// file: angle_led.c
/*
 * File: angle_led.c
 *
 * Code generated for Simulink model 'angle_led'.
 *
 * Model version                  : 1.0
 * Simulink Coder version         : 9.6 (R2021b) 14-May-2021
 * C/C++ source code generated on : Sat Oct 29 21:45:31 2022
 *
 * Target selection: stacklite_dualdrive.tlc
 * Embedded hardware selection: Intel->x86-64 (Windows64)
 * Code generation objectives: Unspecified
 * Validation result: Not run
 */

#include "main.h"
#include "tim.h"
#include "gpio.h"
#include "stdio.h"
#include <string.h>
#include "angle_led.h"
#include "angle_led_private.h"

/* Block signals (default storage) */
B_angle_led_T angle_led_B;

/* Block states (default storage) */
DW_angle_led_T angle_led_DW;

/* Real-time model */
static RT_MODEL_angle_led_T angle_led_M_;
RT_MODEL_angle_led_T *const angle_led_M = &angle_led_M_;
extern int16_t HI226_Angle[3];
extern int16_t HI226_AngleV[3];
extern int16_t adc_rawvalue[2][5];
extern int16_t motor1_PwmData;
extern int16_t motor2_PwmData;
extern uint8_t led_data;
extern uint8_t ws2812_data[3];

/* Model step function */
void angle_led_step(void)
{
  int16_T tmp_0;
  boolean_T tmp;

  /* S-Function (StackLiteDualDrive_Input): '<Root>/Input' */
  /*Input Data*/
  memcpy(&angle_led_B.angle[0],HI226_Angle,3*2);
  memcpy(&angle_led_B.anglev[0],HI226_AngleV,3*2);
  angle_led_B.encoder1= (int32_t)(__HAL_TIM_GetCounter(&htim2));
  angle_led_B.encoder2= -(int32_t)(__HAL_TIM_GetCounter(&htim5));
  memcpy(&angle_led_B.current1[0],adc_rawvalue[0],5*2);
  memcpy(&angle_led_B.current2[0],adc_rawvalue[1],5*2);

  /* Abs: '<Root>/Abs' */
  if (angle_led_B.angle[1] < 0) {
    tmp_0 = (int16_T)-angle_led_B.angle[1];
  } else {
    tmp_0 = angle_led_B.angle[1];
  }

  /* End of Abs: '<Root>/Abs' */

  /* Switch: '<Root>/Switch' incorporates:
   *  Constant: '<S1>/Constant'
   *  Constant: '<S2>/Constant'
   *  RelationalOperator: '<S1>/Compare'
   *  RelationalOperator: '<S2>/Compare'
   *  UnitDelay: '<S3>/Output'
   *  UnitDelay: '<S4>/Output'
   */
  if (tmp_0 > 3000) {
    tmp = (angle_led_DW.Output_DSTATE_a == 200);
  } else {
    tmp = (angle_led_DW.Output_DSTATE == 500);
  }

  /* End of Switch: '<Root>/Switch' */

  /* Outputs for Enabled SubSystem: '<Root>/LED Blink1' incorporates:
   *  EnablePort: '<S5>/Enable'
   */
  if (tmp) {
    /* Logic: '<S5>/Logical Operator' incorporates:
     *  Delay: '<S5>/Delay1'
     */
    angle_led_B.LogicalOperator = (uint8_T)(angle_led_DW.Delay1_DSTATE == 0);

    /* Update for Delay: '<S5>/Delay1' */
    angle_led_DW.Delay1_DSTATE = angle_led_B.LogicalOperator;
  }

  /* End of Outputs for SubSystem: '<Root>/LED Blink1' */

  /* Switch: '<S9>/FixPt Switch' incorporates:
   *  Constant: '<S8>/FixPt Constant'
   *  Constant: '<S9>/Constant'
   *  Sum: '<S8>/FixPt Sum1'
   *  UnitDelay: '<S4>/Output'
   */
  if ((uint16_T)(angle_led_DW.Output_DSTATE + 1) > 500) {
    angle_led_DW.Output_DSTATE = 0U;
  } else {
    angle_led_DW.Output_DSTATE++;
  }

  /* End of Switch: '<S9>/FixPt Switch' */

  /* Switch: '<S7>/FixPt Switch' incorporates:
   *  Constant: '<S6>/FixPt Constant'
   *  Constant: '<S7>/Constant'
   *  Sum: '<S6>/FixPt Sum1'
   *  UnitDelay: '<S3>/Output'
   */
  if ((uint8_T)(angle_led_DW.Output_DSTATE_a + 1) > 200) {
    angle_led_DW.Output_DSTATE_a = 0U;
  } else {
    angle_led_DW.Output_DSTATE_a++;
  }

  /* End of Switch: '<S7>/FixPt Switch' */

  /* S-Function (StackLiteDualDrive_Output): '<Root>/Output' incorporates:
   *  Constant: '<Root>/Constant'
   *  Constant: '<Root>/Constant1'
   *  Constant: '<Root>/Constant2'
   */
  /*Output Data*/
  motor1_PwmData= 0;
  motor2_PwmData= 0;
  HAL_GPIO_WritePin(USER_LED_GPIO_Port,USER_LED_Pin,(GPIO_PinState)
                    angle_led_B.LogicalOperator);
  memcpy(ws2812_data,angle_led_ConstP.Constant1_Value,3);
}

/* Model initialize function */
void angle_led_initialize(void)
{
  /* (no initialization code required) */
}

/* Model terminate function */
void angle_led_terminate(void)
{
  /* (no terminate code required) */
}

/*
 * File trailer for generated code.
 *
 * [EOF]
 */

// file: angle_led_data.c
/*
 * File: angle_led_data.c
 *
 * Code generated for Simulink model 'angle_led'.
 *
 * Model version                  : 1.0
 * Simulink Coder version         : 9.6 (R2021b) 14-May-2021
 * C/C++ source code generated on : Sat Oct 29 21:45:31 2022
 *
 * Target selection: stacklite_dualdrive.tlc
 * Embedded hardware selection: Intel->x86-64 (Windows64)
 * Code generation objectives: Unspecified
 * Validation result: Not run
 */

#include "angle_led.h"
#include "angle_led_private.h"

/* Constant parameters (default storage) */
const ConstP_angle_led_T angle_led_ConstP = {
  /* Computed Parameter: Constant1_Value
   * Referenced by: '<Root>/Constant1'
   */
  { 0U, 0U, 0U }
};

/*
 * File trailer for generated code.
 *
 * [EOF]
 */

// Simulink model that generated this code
simulink model "angle_led"  (R2021b)
settings: Solver=FixedStepDiscrete  StartTime=0.0  StopTime=inf  FixedStep=0.0005  RelTol=1e-3
libraries: simulink x4

== system angle_led ==
  note: angle的单位是0.01度，
      | 即30度输出值为3000
  Abs : Abs
  Compare To Constant : simulink/Logic and Bit Operations/Compare To Constant  relop===  const=200  OutDataTypeStr=boolean
  Compare To Constant1 : simulink/Logic and Bit Operations/Compare To Constant  relop===  const=500  OutDataTypeStr=boolean
  Constant : Constant  Value=0  OutDataTypeStr=int16
  Constant1 : Constant  Value=[0 0 0]  OutDataTypeStr=uint8
  Constant2 : Constant  Value=0  OutDataTypeStr=int16
  Counter Limited : simulink/Sources/Counter Limited  uplimit=200  tsamp=-1
  Counter Limited1 : simulink/Sources/Counter Limited  uplimit=500  tsamp=-1
  Demux : Demux  Outputs=3
  Input : S-Function  Priority=0  FunctionName=StackLiteDualDrive_Input  SFunctionModules=StackLiteDualDrive_Input  SFunctionDeploymentMode=off  EnableBusSupport=off  mask(input){}
      mask help: input
  LED Blink1 : Subsystem
  Output : S-Function  Priority=255  FunctionName=StackLiteDualDrive_Output  SFunctionModules=StackLiteDualDrive_Output  SFunctionDeploymentMode=off  EnableBusSupport=off  mask(output){}
      mask help: output
  Switch : Switch  Criteria=u2 > Threshold  Threshold=3000
  Terminator{,1..6} (7 alike) : Terminator
  wires:
  Constant2/1 -> Output/2
  Compare To Constant/1 -> Switch/1
  Compare To Constant1/1 -> Switch/3  "led"
  Input/5 -> Terminator3/1  "current1"
  Input/6 -> Terminator4/1  "current2"
  Abs/1 -> Switch/2
  Demux/2 -> Abs/1
  Input/3 -> Terminator/1  "encoder1"
  Constant1/1 -> Output/4
  Input/1 -> Demux/1  "angle"
  Demux/3 -> Terminator6/1
  Constant/1 -> Output/1
  LED Blink1/1(Out1) -> Output/3  "led"
  Input/2 -> Terminator1/1  "anglev"
  Input/4 -> Terminator2/1  "encoder2"
  Switch/1 -> LED Blink1/Enable
  Counter Limited1/1 -> Compare To Constant1/1
  Counter Limited/1 -> Compare To Constant/1
  Demux/1 -> Terminator5/1

== system angle_led/LED Blink1 ==
  Enable : EnablePort
  Delay1 : Delay  DelayLength=1  InitialCondition=uint8(0)
  Logical Operator : Logic  Operator=NOT  Inputs=1  AllPortsSameDT=off  OutDataTypeStr=fixdt(0,8)
  Out1 : Outport  VectorParamsAs1DForOutWhenUnconnected=off
  wires:
  Logical Operator/1 -> Out1/1, Delay1/1
  Delay1/1 -> Logical Operator/1
